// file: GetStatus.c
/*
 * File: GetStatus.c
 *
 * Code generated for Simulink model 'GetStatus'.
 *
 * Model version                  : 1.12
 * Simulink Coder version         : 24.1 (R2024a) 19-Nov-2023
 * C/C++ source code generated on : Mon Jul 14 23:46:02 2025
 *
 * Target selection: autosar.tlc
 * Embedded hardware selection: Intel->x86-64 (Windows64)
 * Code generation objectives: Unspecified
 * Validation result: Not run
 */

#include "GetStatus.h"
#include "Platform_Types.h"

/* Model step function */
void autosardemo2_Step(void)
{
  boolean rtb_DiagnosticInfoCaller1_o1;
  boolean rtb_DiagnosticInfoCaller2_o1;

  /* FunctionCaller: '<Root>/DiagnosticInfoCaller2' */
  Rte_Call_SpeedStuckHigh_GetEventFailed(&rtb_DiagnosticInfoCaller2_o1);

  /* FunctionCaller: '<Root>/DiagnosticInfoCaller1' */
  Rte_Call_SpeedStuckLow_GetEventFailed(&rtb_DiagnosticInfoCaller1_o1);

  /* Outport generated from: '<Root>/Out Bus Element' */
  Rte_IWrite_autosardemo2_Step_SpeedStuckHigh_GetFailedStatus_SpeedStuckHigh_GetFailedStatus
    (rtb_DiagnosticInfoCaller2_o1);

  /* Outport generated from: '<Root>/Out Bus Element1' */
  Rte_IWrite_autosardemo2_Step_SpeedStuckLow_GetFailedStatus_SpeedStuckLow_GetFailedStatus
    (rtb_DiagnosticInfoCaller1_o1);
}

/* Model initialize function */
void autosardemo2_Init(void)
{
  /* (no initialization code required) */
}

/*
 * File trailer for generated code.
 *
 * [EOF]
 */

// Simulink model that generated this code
simulink model "GetStatus"  (R2024a)
settings: Solver=FixedStepAuto  StartTime=0.0  StopTime=10.0  RelTol=1e-3
libraries: autosarlibdem x2

== system GetStatus ==
  note: Read DEM Service
  DiagnosticInfoCaller1 : autosarlibdem/DiagnosticInfoCaller  PortName=SpeedStuckLow  Operation=GetEventFailed  st=-1  ServiceImpl=autosar.bsw.DemDiagnosticInfo  SyncToSchema=off
  DiagnosticInfoCaller2 : autosarlibdem/DiagnosticInfoCaller  PortName=SpeedStuckHigh  Operation=GetEventFailed  st=-1  ServiceImpl=autosar.bsw.DemDiagnosticInfo  SyncToSchema=off
  Terminator : Terminator
  Terminator1 : Terminator
  Out Bus Element : Outport  PortName=SpeedStuckHigh_GetFailedStatus  Element=SpeedStuckHigh_GetFailedStatus
  Out Bus Element1 : Outport  Port=2  PortName=SpeedStuckLow_GetFailedStatus  Element=SpeedStuckLow_GetFailedStatus
  wires:
  DiagnosticInfoCaller1/2 -> Terminator1/1
  DiagnosticInfoCaller2/2 -> Terminator/1
  DiagnosticInfoCaller2/1 -> Out Bus Element/1
  DiagnosticInfoCaller1/1 -> Out Bus Element1/1
